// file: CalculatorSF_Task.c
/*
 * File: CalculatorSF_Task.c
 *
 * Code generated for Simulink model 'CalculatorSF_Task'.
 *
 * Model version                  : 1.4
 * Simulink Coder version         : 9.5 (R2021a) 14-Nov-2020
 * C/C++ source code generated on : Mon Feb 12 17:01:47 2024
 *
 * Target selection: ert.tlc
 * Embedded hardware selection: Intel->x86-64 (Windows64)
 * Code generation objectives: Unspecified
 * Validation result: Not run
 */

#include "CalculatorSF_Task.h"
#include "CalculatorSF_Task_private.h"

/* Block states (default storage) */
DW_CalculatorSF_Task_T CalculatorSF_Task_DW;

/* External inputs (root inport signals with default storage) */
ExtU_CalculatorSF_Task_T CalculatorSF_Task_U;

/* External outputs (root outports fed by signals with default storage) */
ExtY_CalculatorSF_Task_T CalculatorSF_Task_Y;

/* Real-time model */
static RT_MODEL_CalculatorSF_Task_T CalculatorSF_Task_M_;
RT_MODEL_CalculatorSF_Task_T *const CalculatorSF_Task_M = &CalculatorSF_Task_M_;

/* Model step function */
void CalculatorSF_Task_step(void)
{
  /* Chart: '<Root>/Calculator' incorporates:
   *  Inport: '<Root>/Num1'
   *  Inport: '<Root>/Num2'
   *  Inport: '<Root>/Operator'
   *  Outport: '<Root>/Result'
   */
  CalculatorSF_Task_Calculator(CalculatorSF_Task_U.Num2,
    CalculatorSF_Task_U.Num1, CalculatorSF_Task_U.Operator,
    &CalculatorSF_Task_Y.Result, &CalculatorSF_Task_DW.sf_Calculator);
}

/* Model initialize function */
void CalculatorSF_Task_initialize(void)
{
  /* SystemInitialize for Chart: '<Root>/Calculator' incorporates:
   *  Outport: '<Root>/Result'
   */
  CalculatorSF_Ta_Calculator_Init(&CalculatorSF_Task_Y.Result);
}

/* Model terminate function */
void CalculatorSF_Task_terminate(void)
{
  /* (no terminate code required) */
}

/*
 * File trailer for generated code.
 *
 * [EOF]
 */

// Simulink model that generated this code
simulink model "CalculatorSF_Task"  (R2021a)
settings: Solver=FixedStepDiscrete  StartTime=0.0  StopTime=10.0  RelTol=1e-3

== system CalculatorSF_Task ==
  Num1 : Inport
  Num2 : Inport  Port=2
  Operator : Inport  Port=3
  Calculator : Stateflow chart  TreatAsAtomicUnit=on
  Result : Outport
  wires:
  Calculator/1(Result) -> Result/1
  Operator/1 -> Calculator/3(Operator)
  Num2/1 -> Calculator/1(Num2)
  Num1/1 -> Calculator/2(Num1)

== stateflow chart CalculatorSF_Task/Calculator ==
  state add(N1,N2) [function]
    (default) -> (junction 24) : {Result = N1 + N2;}
  state Calculator
    (default) -> (junction 49) : % Calculation
    (junction 49) -> (junction 50) [order 1] : [Operator == 0]
    (junction 49) -> (junction 51) [order 2]
    (junction 50) -> (junction 58) : {add(Num1,Num2);}
    (junction 51) -> (junction 52) [order 1] : [Operator == 1]
    (junction 51) -> (junction 53) [order 2]
    (junction 52) -> (junction 57) : {sub(Num1,Num2);}
    (junction 53) -> (junction 54) [order 1] : [Operator == 2]
    (junction 53) -> (junction 55) [order 2] : {divide(Num1,Num2);}
    (junction 54) -> (junction 56) : {multiply(Num1,Num2);}
    (junction 56) -> (junction 55)
    (junction 57) -> (junction 56)
    (junction 58) -> (junction 57)
    (junction 55) -> (junction 59)
  state sub(N1,N2) [function]
    (default) -> (junction 5) : {Result = N1 - N2;}
  state multiply(N1,N2) [function]
    (default) -> (junction 8) : {Result = N1 * N2;}
  state divide(N1,N2) [function]
    (default) -> (junction 14)
    (junction 14) -> (junction 61) [order 1] : [N2 == 0]
    (junction 61) -> (junction 65) : {Result = -1;}
    (junction 14) -> (junction 65) [order 2] : {Result = N1 / N2;}
  (default) -> Calculator
  data: N1 function_input; N2 function_input; N1 function_input; N2 function_input; N1 function_input; N2 function_input; N1 function_input; N2 function_input; Num2 input; Num1 input; Operator input double; Result output
